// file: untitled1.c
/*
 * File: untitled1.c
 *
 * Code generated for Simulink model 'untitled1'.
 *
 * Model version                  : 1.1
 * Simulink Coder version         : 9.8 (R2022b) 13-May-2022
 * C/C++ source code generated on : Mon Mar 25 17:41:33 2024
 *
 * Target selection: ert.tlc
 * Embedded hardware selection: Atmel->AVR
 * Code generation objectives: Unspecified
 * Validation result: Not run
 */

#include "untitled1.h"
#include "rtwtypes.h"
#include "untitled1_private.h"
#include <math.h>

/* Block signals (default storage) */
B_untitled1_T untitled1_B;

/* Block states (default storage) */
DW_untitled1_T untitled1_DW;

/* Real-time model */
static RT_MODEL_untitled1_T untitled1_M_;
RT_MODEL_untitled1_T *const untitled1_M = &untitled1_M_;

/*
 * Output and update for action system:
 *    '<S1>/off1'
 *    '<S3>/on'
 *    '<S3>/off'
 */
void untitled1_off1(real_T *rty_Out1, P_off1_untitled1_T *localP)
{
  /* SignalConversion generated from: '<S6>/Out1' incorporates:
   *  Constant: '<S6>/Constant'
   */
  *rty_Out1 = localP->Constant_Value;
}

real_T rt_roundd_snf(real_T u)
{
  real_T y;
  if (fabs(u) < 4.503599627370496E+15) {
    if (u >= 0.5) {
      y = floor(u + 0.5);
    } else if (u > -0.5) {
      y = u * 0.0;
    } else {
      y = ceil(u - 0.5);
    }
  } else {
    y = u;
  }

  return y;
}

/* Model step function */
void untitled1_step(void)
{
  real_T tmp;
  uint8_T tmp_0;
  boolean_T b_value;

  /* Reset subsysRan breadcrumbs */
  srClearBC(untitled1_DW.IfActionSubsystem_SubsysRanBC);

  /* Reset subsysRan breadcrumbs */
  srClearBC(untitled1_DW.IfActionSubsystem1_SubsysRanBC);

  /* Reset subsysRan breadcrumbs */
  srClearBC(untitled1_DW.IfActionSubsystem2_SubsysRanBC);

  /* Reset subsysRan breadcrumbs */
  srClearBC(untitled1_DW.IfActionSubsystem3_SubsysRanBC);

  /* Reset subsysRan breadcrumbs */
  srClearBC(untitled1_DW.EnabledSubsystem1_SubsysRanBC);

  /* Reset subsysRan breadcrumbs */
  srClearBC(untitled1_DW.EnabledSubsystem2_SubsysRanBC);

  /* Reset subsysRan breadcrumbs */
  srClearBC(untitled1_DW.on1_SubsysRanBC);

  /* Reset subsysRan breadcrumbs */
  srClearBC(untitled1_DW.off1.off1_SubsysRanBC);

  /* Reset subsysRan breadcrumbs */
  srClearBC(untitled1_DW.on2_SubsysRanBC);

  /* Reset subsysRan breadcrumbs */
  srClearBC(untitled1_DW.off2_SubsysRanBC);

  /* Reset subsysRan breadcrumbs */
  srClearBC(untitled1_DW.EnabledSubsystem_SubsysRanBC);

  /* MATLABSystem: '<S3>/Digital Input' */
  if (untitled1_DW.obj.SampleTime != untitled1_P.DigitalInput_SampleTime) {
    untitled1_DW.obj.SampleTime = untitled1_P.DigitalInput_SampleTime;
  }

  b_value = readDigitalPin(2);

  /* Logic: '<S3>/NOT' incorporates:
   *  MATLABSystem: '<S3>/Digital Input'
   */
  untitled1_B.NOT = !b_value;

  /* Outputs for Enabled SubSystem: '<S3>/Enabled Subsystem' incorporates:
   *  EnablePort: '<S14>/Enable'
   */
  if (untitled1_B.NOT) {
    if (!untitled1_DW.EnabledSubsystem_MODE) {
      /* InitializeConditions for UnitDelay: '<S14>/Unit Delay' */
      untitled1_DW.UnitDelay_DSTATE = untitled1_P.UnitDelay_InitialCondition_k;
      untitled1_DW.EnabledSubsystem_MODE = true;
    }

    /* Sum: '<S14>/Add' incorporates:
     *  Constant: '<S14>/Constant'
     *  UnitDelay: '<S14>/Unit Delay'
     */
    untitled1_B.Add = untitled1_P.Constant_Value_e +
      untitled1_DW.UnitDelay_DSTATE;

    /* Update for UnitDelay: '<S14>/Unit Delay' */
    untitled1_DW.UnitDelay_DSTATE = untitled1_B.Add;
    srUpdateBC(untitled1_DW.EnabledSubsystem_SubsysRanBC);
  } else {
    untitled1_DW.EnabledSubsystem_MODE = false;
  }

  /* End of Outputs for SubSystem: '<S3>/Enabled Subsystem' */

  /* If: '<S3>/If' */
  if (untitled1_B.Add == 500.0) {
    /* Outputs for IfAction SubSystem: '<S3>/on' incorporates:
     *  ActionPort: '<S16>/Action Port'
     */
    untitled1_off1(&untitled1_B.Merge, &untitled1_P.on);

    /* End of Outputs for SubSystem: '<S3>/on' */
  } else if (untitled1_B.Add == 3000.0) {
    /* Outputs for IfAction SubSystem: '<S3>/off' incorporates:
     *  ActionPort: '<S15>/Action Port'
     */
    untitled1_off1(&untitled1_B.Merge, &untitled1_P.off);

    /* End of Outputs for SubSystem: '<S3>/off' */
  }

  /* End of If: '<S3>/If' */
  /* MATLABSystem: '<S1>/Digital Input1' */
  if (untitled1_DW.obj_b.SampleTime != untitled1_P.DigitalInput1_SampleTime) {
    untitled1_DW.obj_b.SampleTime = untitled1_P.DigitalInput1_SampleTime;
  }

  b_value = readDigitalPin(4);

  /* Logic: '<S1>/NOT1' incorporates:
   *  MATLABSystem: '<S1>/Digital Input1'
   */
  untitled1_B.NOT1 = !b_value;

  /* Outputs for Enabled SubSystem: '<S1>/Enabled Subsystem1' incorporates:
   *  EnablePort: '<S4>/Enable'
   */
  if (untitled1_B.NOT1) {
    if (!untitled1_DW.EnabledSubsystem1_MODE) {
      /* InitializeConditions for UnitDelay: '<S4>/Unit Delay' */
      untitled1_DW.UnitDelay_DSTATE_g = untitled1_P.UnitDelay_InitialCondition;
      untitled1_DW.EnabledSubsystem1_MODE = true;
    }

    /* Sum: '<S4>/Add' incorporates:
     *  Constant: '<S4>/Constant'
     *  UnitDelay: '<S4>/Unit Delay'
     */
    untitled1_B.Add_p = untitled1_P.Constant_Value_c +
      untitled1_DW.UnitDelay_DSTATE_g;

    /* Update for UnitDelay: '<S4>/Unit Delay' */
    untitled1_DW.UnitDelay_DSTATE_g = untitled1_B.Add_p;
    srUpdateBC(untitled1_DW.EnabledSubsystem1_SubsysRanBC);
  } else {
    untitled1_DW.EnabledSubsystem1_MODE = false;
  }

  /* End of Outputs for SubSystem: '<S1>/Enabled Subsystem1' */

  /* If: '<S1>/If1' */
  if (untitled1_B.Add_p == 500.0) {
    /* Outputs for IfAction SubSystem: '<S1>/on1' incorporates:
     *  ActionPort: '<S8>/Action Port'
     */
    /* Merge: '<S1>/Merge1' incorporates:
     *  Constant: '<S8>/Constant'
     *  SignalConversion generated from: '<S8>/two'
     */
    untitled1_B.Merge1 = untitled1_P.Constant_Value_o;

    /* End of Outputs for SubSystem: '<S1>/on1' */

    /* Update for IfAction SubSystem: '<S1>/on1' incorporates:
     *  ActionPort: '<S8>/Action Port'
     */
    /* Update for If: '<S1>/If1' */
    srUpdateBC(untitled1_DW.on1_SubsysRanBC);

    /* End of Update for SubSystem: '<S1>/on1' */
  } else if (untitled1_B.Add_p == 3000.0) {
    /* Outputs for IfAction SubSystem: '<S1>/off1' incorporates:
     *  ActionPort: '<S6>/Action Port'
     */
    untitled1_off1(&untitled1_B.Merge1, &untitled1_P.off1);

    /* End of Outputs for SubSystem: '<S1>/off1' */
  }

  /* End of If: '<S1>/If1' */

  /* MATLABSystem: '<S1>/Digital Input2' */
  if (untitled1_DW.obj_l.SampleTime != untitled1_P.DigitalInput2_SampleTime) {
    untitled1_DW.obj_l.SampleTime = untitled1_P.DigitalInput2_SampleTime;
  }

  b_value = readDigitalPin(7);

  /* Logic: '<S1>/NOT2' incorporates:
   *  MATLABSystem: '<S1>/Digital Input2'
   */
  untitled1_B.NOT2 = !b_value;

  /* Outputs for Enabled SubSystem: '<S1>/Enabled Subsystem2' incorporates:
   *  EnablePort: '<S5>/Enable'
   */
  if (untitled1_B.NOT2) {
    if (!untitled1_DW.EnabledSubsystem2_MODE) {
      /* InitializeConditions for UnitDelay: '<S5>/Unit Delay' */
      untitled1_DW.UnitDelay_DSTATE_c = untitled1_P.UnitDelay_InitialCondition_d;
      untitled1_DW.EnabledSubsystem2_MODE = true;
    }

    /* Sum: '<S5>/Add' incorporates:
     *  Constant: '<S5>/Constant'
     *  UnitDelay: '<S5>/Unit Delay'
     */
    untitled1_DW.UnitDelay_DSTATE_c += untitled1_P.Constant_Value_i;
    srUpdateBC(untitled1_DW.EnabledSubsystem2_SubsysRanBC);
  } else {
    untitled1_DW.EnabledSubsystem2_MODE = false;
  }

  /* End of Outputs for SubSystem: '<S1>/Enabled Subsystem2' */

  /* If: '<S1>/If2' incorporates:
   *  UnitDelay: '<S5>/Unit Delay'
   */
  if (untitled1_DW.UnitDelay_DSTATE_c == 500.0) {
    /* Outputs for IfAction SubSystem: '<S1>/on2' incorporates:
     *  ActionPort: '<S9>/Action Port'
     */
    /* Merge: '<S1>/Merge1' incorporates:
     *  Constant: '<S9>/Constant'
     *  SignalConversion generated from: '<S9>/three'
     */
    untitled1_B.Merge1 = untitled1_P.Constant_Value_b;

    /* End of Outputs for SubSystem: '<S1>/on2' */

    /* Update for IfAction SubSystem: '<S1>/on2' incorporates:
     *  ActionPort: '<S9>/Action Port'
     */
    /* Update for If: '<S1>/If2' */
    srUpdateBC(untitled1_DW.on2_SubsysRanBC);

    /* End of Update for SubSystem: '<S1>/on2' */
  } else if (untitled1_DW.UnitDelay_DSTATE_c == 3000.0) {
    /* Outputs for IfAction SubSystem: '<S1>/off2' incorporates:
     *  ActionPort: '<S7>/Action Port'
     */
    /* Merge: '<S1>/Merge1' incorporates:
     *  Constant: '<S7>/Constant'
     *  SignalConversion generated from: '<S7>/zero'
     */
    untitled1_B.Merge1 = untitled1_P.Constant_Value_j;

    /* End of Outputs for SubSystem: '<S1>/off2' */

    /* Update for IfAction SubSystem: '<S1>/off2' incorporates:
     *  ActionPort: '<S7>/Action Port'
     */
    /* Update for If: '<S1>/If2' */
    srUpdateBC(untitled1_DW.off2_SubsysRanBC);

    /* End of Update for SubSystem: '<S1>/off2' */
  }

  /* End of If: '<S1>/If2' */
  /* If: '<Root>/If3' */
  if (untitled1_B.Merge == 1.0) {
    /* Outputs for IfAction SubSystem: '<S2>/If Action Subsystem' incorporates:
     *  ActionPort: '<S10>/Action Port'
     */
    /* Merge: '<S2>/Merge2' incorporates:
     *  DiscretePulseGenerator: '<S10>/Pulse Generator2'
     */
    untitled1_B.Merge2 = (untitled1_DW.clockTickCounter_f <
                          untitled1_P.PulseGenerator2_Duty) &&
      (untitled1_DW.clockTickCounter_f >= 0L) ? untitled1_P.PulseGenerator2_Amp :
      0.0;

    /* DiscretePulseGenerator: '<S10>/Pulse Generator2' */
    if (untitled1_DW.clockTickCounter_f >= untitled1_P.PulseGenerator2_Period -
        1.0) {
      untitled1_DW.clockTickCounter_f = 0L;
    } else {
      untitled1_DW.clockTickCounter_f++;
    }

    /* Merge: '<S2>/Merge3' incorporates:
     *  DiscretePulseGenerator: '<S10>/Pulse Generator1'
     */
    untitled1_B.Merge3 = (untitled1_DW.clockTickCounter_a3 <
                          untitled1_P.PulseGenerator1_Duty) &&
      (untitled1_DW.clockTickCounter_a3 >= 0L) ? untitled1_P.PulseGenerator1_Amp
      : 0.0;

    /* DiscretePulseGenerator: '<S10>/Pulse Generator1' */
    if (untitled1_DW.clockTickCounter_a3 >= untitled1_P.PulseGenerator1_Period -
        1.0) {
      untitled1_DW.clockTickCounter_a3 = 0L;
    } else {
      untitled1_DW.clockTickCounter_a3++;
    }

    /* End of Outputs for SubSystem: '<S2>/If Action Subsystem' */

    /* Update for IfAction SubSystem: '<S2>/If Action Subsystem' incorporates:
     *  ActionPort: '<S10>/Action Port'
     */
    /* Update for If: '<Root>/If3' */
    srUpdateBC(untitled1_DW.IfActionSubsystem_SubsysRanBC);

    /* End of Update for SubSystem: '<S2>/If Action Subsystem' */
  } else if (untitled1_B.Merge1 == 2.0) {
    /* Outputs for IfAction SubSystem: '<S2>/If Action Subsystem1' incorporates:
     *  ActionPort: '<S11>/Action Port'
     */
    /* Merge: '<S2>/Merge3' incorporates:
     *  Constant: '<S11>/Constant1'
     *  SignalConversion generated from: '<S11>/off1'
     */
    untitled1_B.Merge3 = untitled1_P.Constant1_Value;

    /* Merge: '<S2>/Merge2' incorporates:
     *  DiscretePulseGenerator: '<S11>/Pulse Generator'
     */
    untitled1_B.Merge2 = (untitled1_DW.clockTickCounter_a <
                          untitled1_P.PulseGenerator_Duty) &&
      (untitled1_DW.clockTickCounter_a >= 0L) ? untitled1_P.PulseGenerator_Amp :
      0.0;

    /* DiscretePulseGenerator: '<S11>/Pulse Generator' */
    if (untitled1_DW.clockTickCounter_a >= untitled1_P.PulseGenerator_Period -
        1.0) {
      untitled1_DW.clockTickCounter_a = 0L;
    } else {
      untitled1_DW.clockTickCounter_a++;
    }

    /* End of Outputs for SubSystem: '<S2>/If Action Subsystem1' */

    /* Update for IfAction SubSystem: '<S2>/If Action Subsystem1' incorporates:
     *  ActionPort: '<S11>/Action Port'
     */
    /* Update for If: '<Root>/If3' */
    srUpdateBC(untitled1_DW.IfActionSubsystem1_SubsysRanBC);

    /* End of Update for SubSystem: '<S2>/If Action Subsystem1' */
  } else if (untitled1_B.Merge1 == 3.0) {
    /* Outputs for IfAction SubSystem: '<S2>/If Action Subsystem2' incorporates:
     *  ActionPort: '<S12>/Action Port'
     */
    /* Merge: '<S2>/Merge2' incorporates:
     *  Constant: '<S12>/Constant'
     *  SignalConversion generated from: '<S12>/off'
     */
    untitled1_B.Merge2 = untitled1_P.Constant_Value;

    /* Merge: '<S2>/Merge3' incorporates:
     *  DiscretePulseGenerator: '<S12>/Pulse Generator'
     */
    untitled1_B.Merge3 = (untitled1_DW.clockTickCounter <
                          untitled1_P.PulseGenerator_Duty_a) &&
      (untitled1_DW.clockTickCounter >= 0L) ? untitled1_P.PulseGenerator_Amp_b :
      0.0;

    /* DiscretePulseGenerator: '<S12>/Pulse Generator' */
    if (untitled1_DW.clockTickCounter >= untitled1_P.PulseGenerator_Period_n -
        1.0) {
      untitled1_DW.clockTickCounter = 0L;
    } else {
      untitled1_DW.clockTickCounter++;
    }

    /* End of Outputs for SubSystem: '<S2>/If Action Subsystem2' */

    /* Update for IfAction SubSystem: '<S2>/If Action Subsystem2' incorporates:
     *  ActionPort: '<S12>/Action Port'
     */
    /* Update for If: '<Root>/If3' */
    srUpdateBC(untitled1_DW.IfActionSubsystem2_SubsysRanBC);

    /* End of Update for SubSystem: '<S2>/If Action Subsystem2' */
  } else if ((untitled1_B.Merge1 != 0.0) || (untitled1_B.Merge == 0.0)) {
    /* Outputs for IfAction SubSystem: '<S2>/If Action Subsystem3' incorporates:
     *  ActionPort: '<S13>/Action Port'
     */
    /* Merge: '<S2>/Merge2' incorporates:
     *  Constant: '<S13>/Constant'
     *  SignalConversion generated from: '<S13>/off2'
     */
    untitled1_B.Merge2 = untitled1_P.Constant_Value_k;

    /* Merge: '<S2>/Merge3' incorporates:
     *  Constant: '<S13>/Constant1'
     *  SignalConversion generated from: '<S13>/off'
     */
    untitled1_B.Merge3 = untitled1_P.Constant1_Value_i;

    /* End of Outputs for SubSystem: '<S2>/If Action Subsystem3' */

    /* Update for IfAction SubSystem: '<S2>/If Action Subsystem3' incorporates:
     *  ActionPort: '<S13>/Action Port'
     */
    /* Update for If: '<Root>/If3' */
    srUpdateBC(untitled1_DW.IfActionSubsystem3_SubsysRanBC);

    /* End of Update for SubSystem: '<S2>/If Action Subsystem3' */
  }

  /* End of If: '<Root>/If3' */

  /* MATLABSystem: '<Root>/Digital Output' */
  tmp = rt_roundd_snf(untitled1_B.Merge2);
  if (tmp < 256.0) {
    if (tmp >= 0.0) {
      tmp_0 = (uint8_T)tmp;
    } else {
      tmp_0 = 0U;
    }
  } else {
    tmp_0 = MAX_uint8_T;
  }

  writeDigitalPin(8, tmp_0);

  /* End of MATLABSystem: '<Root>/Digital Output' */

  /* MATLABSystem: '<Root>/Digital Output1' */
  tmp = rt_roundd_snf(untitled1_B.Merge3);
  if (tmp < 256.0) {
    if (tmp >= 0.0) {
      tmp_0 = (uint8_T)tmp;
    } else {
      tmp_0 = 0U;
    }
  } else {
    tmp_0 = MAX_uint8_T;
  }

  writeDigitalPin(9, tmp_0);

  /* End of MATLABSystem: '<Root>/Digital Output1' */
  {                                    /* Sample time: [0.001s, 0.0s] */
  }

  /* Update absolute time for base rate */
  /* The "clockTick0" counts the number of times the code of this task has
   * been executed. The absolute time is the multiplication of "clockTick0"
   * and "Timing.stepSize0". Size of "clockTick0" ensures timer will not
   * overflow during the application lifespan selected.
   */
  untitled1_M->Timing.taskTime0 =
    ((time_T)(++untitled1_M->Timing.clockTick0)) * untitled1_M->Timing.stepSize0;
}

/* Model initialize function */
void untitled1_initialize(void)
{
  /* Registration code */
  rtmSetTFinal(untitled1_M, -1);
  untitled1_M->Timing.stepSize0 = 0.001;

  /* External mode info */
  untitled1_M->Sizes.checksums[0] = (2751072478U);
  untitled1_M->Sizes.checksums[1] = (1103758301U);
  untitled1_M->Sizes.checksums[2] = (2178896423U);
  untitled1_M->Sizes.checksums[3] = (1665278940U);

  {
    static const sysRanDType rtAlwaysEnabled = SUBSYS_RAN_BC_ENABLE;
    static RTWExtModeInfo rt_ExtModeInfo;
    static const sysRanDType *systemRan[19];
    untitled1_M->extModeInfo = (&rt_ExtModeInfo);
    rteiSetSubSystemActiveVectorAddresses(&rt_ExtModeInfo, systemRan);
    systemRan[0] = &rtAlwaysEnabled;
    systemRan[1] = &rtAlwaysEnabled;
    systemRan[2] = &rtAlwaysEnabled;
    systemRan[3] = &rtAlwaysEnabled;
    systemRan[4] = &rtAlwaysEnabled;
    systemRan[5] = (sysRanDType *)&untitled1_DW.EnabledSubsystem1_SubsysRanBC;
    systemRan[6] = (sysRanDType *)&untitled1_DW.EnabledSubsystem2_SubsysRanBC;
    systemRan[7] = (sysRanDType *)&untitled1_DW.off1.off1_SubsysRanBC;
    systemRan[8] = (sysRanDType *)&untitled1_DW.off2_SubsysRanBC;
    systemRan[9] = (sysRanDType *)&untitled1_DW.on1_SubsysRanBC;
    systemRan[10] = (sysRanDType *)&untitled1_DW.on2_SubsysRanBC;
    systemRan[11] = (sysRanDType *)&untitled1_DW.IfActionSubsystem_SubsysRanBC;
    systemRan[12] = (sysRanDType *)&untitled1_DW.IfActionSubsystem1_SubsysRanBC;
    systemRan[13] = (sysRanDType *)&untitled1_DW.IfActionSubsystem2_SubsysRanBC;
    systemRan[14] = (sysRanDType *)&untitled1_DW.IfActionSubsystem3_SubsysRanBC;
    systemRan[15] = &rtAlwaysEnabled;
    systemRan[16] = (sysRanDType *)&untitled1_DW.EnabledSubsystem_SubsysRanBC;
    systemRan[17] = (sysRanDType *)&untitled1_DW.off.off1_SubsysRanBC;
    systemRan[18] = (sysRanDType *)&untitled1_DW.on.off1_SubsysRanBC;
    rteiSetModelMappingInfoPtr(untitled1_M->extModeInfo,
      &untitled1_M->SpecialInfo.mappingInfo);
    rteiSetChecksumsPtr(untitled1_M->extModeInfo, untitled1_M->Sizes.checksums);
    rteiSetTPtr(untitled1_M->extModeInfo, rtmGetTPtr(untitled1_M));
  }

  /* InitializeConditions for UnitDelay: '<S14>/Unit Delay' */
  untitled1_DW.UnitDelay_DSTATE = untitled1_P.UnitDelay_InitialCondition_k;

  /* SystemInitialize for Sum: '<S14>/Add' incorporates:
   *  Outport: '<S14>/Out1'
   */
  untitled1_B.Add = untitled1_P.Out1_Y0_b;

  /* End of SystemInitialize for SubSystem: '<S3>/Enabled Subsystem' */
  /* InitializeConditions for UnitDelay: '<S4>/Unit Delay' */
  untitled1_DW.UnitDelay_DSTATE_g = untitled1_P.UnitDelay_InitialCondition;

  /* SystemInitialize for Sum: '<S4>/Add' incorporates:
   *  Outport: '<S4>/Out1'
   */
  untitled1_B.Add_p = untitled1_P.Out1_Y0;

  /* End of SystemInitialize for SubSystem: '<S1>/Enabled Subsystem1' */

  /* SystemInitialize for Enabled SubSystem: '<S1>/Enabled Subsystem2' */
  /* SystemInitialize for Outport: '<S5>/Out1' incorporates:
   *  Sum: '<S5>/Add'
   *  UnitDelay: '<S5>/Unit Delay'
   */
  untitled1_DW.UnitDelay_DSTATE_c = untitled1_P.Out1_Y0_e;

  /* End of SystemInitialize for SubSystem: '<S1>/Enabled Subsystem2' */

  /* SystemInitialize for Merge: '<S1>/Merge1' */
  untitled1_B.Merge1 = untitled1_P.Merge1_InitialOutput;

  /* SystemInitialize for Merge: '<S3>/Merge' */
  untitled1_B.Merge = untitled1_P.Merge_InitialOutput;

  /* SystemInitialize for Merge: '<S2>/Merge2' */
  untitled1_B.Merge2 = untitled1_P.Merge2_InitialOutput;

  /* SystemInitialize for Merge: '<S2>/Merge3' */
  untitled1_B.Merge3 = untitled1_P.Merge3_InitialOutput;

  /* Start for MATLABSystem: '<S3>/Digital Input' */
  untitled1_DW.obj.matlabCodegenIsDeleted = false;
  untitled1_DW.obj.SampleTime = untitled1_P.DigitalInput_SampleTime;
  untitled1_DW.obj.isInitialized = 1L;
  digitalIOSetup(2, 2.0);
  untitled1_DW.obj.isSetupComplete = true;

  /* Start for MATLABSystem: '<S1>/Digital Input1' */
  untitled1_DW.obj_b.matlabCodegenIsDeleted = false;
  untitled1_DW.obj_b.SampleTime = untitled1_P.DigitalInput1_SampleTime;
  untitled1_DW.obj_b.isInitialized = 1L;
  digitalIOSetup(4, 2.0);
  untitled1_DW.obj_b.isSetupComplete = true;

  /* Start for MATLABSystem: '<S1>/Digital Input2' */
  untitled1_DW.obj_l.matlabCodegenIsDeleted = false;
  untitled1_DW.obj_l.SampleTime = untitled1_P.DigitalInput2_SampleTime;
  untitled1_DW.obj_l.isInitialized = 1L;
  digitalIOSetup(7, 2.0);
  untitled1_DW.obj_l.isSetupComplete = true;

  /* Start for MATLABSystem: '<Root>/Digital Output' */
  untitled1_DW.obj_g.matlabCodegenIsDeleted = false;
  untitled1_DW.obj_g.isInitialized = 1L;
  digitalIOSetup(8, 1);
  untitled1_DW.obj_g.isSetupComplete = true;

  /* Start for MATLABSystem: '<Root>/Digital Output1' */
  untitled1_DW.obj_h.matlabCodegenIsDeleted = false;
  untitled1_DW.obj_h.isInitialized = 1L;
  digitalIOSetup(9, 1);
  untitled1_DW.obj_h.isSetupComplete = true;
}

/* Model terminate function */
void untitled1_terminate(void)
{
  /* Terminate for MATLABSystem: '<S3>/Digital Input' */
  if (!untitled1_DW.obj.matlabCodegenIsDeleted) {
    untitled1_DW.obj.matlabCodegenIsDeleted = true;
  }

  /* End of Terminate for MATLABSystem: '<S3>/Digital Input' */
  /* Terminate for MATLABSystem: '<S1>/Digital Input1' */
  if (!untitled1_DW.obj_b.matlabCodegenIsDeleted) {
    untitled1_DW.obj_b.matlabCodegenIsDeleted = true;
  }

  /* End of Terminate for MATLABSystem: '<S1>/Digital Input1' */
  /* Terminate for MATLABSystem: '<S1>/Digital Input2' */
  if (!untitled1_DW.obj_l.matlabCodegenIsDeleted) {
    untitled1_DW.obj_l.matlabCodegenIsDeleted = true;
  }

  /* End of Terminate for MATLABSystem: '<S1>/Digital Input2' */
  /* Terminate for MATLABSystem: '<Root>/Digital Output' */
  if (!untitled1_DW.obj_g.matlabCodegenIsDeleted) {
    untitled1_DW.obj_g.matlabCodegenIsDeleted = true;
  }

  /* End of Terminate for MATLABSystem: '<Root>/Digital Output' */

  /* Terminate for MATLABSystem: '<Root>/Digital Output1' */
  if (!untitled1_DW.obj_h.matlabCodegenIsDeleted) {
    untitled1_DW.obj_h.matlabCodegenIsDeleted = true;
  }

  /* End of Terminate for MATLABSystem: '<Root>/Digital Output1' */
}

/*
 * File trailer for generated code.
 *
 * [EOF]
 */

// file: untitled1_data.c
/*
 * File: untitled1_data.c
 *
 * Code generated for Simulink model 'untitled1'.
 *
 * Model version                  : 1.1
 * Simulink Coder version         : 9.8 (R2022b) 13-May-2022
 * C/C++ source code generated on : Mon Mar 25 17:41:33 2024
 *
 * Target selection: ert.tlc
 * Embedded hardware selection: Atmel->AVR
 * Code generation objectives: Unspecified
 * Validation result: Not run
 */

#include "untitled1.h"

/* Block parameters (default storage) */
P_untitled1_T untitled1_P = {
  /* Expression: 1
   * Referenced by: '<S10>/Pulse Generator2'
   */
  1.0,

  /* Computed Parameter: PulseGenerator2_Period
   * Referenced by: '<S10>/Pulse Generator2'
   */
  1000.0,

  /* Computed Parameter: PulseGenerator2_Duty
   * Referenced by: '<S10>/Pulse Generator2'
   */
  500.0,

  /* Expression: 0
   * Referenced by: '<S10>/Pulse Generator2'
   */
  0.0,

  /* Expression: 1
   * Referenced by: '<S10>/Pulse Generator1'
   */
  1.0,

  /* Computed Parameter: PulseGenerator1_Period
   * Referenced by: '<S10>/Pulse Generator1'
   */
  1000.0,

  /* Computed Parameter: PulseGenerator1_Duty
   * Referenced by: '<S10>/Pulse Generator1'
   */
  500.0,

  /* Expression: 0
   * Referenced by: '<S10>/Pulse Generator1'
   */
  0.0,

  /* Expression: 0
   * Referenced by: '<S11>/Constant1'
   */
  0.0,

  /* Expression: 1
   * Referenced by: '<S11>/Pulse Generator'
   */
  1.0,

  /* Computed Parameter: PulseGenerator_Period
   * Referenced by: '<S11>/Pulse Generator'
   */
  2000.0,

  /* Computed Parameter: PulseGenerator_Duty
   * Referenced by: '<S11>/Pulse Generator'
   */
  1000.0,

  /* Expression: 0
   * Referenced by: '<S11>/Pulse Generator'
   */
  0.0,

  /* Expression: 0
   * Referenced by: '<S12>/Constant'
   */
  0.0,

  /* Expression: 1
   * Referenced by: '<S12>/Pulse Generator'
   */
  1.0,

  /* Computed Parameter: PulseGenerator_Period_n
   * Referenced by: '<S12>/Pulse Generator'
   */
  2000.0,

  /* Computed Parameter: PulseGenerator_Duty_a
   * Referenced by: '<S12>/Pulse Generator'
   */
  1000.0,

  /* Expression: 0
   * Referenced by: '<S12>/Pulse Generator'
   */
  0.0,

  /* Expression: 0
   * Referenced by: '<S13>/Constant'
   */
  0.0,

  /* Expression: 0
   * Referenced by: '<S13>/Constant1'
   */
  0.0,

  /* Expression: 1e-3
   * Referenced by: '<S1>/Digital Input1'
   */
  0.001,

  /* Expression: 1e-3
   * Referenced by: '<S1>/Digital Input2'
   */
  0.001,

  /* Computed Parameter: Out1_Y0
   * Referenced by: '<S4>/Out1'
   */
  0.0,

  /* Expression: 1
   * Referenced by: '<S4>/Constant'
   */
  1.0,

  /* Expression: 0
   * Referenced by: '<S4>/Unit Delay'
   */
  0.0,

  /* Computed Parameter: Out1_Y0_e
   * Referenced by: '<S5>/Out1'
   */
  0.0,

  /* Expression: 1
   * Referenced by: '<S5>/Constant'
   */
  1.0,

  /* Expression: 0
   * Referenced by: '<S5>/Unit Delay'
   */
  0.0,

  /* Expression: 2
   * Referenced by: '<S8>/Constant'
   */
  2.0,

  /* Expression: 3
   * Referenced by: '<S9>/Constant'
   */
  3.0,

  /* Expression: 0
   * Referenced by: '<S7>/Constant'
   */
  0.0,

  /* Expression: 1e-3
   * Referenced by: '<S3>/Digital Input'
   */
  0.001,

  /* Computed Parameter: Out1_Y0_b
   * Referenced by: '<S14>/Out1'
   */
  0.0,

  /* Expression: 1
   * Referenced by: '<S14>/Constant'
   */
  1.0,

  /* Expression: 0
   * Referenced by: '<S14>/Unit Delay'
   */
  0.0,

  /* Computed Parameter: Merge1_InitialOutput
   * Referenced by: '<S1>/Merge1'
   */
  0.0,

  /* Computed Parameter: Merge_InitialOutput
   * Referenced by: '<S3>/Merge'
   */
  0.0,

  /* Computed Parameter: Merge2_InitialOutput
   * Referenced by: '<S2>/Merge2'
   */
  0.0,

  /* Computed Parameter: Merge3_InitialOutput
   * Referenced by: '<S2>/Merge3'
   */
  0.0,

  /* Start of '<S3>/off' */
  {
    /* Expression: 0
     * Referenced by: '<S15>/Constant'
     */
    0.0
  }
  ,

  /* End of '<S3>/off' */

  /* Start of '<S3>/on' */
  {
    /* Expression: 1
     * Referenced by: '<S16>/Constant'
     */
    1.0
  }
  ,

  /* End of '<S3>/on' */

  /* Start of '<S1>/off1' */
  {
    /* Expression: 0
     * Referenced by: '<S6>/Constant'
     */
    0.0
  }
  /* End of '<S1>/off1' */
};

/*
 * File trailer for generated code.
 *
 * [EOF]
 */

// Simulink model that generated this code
simulink model "untitled1"  (R2022b)
settings: Solver=FixedStepDiscrete  StartTime=0.0  StopTime=inf  FixedStep=1e-3  RelTol=1e-3  EnableMultiTasking=on
libraries: arduinolib x5

== system untitled1 ==
  Digital Output : arduinolib/Digital Output  pinNumber=8  Direction=output  blockPlatform=arduino
  Digital Output1 : arduinolib/Digital Output  pinNumber=9  Direction=output  blockPlatform=arduino
  If3 : If  NumInputs=2  IfExpression=u1 ==1  ElseIfExpressions=u2==2,u2==3,u2|u1==0  ShowElse=off
  push_buttom on\off2 : Subsystem
  signals_organization : Subsystem
  switch_bettween_2buttom : Subsystem
  wires:
  switch_bettween_2buttom/1(Out1) -> If3/1
  signals_organization/1(Out1) -> Digital Output/1
  If3/2 -> signals_organization/2(Action Port1)
  If3/1 -> signals_organization/1(Action Port)
  signals_organization/2(Out2) -> Digital Output1/1
  If3/3 -> signals_organization/3(Action Port2)
  push_buttom on\off2/1(Out1) -> If3/2
  If3/4 -> signals_organization/4(Action Port3)

== system untitled1/push_buttom on\off2 ==
  Digital Input1 : arduinolib/Digital Input  pinNumber=4  mode=Input Pullup  Direction=input  SampleTime=1e-3  blockPlatform=arduino
  Digital Input2 : arduinolib/Digital Input  pinNumber=7  mode=Input Pullup  Direction=input  SampleTime=1e-3  blockPlatform=arduino
  Display3 : Display
  Display4 : Display
  Enabled Subsystem1 : Subsystem  TreatAsAtomicUnit=on
  Enabled Subsystem2 : Subsystem  TreatAsAtomicUnit=on
  If1 : If  IfExpression=u1 ==500  ElseIfExpressions=u1 ==3000  ShowElse=off
  If2 : If  IfExpression=u1 ==500  ElseIfExpressions=u1 ==3000  ShowElse=off
  Merge1 : Merge  Inputs=4
  NOT1 : Logic  Operator=NOT  IconShape=distinctive  AllPortsSameDT=off  OutDataTypeStr=boolean
  NOT2 : Logic  Operator=NOT  IconShape=distinctive  AllPortsSameDT=off  OutDataTypeStr=boolean
  off1 : Subsystem  TreatAsAtomicUnit=on
  off2 : Subsystem  TreatAsAtomicUnit=on
  on1 : Subsystem  TreatAsAtomicUnit=on
  on2 : Subsystem  TreatAsAtomicUnit=on
  Out1 : Outport
  wires:
  If2/1 -> on2/Action
  If1/2 -> off1/Action
  NOT2/1 -> Display4/1, Enabled Subsystem2/Enable
  Digital Input1/1 -> NOT1/1
  Enabled Subsystem1/1(Out1) -> If1/1
  If2/2 -> off2/Action
  off1/1(Out1) -> Merge1/2
  off2/1(zero) -> Merge1/4
  NOT1/1 -> Display3/1, Enabled Subsystem1/Enable
  Enabled Subsystem2/1(Out1) -> If2/1
  If1/1 -> on1/Action
  on1/1(two) -> Merge1/1
  on2/1(three) -> Merge1/3
  Digital Input2/1 -> NOT2/1
  Merge1/1 -> Out1/1

== system untitled1/signals_organization ==
  Action Port : Inport
  Action Port1 : Inport  Port=2
  Action Port2 : Inport  Port=3
  Action Port3 : Inport  Port=4
  If Action Subsystem : Subsystem  TreatAsAtomicUnit=on
  If Action Subsystem1 : Subsystem  TreatAsAtomicUnit=on
  If Action Subsystem2 : Subsystem  TreatAsAtomicUnit=on
  If Action Subsystem3 : Subsystem  TreatAsAtomicUnit=on
  Merge2 : Merge  Inputs=4
  Merge3 : Merge  Inputs=4
  Out1 : Outport
  Out2 : Outport  Port=2
  wires:
  Action Port3/1 -> If Action Subsystem3/Action
  If Action Subsystem/2(on2) -> Merge3/1
  If Action Subsystem3/2(off) -> Merge3/4
  If Action Subsystem1/2(off1) -> Merge3/2
  If Action Subsystem1/1(on1) -> Merge2/2
  If Action Subsystem2/1(off) -> Merge2/3
  Action Port1/1 -> If Action Subsystem1/Action
  If Action Subsystem2/2(on) -> Merge3/3
  Merge3/1 -> Out2/1
  If Action Subsystem3/1(off2) -> Merge2/4
  If Action Subsystem/1(on1) -> Merge2/1
  Action Port2/1 -> If Action Subsystem2/Action
  Action Port/1 -> If Action Subsystem/Action
  Merge2/1 -> Out1/1

== system untitled1/switch_bettween_2buttom ==
  Digital Input : arduinolib/Digital Input  pinNumber=2  mode=Input Pullup  Direction=input  SampleTime=1e-3  blockPlatform=arduino
  Display : Display
  Enabled Subsystem : Subsystem  TreatAsAtomicUnit=on
  If : If  IfExpression=u1 ==500  ElseIfExpressions=u1 ==3000  ShowElse=off
  Merge : Merge
  NOT : Logic  Operator=NOT  IconShape=distinctive  AllPortsSameDT=off  OutDataTypeStr=boolean
  off : Subsystem  TreatAsAtomicUnit=on
  on : Subsystem  TreatAsAtomicUnit=on
  Out1 : Outport
  wires:
  If/2 -> off/Action
  Digital Input/1 -> NOT/1
  If/1 -> on/Action
  Enabled Subsystem/1(Out1) -> If/1
  on/1(Out1) -> Merge/1
  NOT/1 -> Display/1, Enabled Subsystem/Enable
  off/1(Out1) -> Merge/2
  Merge/1 -> Out1/1

== system untitled1/push_buttom on\off2/Enabled Subsystem1 ==
  Enable : EnablePort  StatesWhenEnabling=reset
  Add : Sum
  Constant : Constant
  Display : Display
  Unit Delay : UnitDelay  SampleTime=-1  HasFrameUpgradeWarning=on
  Out1 : Outport
  wires:
  Unit Delay/1 -> Add/2
  Add/1 -> Display/1, Out1/1, Unit Delay/1
  Constant/1 -> Add/1

== system untitled1/push_buttom on\off2/Enabled Subsystem2 ==
  Enable : EnablePort  StatesWhenEnabling=reset
  Add : Sum
  Constant : Constant
  Unit Delay : UnitDelay  SampleTime=-1  HasFrameUpgradeWarning=on
  Out1 : Outport
  wires:
  Constant/1 -> Add/1
  Add/1 -> Unit Delay/1, Out1/1
  Unit Delay/1 -> Add/2

== system untitled1/push_buttom on\off2/off1 ==
  Action Port : ActionPort  ActionPortLabel=elseif(u1 ==3000)
  Constant : Constant  Value=0
  Out1 : Outport
  wires:
  Constant/1 -> Out1/1

== system untitled1/push_buttom on\off2/off2 ==
  Action Port : ActionPort  ActionPortLabel=elseif(u1 ==3000)
  Constant : Constant  Value=0
  zero : Outport
  wires:
  Constant/1 -> zero/1

== system untitled1/push_buttom on\off2/on1 ==
  Action Port : ActionPort  ActionPortLabel=if(u1 ==500)
  Constant : Constant  Value=2
  two : Outport
  wires:
  Constant/1 -> two/1

== system untitled1/push_buttom on\off2/on2 ==
  Action Port : ActionPort  ActionPortLabel=if(u1 ==500)
  Constant : Constant  Value=3
  three : Outport
  wires:
  Constant/1 -> three/1

== system untitled1/signals_organization/If Action Subsystem ==
  Action Port : ActionPort  ActionPortLabel=if(u1 ==1)
  Pulse Generator1 : DiscretePulseGenerator  PulseType=Time based  Period=1  PulseWidth=50
  Pulse Generator2 : DiscretePulseGenerator  PulseType=Time based  Period=1  PulseWidth=50
  on1 : Outport
  on2 : Outport  Port=2
  wires:
  Pulse Generator2/1 -> on1/1
  Pulse Generator1/1 -> on2/1

== system untitled1/signals_organization/If Action Subsystem1 ==
  Action Port : ActionPort  ActionPortLabel=elseif(u2==2)
  Constant1 : Constant  Value=0
  Pulse Generator : DiscretePulseGenerator  PulseType=Time based  PulseWidth=50
  on1 : Outport
  off1 : Outport  Port=2
  wires:
  Constant1/1 -> off1/1
  Pulse Generator/1 -> on1/1

== system untitled1/signals_organization/If Action Subsystem2 ==
  Action Port : ActionPort  ActionPortLabel=elseif(u2==3)
  Constant : Constant  Value=0
  Pulse Generator : DiscretePulseGenerator  PulseType=Time based  PulseWidth=50
  off : Outport
  on : Outport  Port=2
  wires:
  Constant/1 -> off/1
  Pulse Generator/1 -> on/1

== system untitled1/signals_organization/If Action Subsystem3 ==
  Action Port : ActionPort  ActionPortLabel=elseif(u2|u1==0)
  Constant : Constant  Value=0
  Constant1 : Constant  Value=0
  off2 : Outport
  off : Outport  Port=2
  wires:
  Constant/1 -> off2/1
  Constant1/1 -> off/1

== system untitled1/switch_bettween_2buttom/Enabled Subsystem ==
  Enable : EnablePort  StatesWhenEnabling=reset
  Add : Sum
  Constant : Constant
  Display : Display
  Unit Delay : UnitDelay  SampleTime=-1  HasFrameUpgradeWarning=on
  Out1 : Outport
  wires:
  Constant/1 -> Add/1
  Add/1 -> Unit Delay/1, Display/1, Out1/1
  Unit Delay/1 -> Add/2

== system untitled1/switch_bettween_2buttom/off ==
  Action Port : ActionPort  ActionPortLabel=elseif(u1 ==3000)
  Constant : Constant  Value=0
  Out1 : Outport
  wires:
  Constant/1 -> Out1/1

== system untitled1/switch_bettween_2buttom/on ==
  Action Port : ActionPort  ActionPortLabel=if(u1 ==500)
  Constant : Constant
  Out1 : Outport
  wires:
  Constant/1 -> Out1/1
